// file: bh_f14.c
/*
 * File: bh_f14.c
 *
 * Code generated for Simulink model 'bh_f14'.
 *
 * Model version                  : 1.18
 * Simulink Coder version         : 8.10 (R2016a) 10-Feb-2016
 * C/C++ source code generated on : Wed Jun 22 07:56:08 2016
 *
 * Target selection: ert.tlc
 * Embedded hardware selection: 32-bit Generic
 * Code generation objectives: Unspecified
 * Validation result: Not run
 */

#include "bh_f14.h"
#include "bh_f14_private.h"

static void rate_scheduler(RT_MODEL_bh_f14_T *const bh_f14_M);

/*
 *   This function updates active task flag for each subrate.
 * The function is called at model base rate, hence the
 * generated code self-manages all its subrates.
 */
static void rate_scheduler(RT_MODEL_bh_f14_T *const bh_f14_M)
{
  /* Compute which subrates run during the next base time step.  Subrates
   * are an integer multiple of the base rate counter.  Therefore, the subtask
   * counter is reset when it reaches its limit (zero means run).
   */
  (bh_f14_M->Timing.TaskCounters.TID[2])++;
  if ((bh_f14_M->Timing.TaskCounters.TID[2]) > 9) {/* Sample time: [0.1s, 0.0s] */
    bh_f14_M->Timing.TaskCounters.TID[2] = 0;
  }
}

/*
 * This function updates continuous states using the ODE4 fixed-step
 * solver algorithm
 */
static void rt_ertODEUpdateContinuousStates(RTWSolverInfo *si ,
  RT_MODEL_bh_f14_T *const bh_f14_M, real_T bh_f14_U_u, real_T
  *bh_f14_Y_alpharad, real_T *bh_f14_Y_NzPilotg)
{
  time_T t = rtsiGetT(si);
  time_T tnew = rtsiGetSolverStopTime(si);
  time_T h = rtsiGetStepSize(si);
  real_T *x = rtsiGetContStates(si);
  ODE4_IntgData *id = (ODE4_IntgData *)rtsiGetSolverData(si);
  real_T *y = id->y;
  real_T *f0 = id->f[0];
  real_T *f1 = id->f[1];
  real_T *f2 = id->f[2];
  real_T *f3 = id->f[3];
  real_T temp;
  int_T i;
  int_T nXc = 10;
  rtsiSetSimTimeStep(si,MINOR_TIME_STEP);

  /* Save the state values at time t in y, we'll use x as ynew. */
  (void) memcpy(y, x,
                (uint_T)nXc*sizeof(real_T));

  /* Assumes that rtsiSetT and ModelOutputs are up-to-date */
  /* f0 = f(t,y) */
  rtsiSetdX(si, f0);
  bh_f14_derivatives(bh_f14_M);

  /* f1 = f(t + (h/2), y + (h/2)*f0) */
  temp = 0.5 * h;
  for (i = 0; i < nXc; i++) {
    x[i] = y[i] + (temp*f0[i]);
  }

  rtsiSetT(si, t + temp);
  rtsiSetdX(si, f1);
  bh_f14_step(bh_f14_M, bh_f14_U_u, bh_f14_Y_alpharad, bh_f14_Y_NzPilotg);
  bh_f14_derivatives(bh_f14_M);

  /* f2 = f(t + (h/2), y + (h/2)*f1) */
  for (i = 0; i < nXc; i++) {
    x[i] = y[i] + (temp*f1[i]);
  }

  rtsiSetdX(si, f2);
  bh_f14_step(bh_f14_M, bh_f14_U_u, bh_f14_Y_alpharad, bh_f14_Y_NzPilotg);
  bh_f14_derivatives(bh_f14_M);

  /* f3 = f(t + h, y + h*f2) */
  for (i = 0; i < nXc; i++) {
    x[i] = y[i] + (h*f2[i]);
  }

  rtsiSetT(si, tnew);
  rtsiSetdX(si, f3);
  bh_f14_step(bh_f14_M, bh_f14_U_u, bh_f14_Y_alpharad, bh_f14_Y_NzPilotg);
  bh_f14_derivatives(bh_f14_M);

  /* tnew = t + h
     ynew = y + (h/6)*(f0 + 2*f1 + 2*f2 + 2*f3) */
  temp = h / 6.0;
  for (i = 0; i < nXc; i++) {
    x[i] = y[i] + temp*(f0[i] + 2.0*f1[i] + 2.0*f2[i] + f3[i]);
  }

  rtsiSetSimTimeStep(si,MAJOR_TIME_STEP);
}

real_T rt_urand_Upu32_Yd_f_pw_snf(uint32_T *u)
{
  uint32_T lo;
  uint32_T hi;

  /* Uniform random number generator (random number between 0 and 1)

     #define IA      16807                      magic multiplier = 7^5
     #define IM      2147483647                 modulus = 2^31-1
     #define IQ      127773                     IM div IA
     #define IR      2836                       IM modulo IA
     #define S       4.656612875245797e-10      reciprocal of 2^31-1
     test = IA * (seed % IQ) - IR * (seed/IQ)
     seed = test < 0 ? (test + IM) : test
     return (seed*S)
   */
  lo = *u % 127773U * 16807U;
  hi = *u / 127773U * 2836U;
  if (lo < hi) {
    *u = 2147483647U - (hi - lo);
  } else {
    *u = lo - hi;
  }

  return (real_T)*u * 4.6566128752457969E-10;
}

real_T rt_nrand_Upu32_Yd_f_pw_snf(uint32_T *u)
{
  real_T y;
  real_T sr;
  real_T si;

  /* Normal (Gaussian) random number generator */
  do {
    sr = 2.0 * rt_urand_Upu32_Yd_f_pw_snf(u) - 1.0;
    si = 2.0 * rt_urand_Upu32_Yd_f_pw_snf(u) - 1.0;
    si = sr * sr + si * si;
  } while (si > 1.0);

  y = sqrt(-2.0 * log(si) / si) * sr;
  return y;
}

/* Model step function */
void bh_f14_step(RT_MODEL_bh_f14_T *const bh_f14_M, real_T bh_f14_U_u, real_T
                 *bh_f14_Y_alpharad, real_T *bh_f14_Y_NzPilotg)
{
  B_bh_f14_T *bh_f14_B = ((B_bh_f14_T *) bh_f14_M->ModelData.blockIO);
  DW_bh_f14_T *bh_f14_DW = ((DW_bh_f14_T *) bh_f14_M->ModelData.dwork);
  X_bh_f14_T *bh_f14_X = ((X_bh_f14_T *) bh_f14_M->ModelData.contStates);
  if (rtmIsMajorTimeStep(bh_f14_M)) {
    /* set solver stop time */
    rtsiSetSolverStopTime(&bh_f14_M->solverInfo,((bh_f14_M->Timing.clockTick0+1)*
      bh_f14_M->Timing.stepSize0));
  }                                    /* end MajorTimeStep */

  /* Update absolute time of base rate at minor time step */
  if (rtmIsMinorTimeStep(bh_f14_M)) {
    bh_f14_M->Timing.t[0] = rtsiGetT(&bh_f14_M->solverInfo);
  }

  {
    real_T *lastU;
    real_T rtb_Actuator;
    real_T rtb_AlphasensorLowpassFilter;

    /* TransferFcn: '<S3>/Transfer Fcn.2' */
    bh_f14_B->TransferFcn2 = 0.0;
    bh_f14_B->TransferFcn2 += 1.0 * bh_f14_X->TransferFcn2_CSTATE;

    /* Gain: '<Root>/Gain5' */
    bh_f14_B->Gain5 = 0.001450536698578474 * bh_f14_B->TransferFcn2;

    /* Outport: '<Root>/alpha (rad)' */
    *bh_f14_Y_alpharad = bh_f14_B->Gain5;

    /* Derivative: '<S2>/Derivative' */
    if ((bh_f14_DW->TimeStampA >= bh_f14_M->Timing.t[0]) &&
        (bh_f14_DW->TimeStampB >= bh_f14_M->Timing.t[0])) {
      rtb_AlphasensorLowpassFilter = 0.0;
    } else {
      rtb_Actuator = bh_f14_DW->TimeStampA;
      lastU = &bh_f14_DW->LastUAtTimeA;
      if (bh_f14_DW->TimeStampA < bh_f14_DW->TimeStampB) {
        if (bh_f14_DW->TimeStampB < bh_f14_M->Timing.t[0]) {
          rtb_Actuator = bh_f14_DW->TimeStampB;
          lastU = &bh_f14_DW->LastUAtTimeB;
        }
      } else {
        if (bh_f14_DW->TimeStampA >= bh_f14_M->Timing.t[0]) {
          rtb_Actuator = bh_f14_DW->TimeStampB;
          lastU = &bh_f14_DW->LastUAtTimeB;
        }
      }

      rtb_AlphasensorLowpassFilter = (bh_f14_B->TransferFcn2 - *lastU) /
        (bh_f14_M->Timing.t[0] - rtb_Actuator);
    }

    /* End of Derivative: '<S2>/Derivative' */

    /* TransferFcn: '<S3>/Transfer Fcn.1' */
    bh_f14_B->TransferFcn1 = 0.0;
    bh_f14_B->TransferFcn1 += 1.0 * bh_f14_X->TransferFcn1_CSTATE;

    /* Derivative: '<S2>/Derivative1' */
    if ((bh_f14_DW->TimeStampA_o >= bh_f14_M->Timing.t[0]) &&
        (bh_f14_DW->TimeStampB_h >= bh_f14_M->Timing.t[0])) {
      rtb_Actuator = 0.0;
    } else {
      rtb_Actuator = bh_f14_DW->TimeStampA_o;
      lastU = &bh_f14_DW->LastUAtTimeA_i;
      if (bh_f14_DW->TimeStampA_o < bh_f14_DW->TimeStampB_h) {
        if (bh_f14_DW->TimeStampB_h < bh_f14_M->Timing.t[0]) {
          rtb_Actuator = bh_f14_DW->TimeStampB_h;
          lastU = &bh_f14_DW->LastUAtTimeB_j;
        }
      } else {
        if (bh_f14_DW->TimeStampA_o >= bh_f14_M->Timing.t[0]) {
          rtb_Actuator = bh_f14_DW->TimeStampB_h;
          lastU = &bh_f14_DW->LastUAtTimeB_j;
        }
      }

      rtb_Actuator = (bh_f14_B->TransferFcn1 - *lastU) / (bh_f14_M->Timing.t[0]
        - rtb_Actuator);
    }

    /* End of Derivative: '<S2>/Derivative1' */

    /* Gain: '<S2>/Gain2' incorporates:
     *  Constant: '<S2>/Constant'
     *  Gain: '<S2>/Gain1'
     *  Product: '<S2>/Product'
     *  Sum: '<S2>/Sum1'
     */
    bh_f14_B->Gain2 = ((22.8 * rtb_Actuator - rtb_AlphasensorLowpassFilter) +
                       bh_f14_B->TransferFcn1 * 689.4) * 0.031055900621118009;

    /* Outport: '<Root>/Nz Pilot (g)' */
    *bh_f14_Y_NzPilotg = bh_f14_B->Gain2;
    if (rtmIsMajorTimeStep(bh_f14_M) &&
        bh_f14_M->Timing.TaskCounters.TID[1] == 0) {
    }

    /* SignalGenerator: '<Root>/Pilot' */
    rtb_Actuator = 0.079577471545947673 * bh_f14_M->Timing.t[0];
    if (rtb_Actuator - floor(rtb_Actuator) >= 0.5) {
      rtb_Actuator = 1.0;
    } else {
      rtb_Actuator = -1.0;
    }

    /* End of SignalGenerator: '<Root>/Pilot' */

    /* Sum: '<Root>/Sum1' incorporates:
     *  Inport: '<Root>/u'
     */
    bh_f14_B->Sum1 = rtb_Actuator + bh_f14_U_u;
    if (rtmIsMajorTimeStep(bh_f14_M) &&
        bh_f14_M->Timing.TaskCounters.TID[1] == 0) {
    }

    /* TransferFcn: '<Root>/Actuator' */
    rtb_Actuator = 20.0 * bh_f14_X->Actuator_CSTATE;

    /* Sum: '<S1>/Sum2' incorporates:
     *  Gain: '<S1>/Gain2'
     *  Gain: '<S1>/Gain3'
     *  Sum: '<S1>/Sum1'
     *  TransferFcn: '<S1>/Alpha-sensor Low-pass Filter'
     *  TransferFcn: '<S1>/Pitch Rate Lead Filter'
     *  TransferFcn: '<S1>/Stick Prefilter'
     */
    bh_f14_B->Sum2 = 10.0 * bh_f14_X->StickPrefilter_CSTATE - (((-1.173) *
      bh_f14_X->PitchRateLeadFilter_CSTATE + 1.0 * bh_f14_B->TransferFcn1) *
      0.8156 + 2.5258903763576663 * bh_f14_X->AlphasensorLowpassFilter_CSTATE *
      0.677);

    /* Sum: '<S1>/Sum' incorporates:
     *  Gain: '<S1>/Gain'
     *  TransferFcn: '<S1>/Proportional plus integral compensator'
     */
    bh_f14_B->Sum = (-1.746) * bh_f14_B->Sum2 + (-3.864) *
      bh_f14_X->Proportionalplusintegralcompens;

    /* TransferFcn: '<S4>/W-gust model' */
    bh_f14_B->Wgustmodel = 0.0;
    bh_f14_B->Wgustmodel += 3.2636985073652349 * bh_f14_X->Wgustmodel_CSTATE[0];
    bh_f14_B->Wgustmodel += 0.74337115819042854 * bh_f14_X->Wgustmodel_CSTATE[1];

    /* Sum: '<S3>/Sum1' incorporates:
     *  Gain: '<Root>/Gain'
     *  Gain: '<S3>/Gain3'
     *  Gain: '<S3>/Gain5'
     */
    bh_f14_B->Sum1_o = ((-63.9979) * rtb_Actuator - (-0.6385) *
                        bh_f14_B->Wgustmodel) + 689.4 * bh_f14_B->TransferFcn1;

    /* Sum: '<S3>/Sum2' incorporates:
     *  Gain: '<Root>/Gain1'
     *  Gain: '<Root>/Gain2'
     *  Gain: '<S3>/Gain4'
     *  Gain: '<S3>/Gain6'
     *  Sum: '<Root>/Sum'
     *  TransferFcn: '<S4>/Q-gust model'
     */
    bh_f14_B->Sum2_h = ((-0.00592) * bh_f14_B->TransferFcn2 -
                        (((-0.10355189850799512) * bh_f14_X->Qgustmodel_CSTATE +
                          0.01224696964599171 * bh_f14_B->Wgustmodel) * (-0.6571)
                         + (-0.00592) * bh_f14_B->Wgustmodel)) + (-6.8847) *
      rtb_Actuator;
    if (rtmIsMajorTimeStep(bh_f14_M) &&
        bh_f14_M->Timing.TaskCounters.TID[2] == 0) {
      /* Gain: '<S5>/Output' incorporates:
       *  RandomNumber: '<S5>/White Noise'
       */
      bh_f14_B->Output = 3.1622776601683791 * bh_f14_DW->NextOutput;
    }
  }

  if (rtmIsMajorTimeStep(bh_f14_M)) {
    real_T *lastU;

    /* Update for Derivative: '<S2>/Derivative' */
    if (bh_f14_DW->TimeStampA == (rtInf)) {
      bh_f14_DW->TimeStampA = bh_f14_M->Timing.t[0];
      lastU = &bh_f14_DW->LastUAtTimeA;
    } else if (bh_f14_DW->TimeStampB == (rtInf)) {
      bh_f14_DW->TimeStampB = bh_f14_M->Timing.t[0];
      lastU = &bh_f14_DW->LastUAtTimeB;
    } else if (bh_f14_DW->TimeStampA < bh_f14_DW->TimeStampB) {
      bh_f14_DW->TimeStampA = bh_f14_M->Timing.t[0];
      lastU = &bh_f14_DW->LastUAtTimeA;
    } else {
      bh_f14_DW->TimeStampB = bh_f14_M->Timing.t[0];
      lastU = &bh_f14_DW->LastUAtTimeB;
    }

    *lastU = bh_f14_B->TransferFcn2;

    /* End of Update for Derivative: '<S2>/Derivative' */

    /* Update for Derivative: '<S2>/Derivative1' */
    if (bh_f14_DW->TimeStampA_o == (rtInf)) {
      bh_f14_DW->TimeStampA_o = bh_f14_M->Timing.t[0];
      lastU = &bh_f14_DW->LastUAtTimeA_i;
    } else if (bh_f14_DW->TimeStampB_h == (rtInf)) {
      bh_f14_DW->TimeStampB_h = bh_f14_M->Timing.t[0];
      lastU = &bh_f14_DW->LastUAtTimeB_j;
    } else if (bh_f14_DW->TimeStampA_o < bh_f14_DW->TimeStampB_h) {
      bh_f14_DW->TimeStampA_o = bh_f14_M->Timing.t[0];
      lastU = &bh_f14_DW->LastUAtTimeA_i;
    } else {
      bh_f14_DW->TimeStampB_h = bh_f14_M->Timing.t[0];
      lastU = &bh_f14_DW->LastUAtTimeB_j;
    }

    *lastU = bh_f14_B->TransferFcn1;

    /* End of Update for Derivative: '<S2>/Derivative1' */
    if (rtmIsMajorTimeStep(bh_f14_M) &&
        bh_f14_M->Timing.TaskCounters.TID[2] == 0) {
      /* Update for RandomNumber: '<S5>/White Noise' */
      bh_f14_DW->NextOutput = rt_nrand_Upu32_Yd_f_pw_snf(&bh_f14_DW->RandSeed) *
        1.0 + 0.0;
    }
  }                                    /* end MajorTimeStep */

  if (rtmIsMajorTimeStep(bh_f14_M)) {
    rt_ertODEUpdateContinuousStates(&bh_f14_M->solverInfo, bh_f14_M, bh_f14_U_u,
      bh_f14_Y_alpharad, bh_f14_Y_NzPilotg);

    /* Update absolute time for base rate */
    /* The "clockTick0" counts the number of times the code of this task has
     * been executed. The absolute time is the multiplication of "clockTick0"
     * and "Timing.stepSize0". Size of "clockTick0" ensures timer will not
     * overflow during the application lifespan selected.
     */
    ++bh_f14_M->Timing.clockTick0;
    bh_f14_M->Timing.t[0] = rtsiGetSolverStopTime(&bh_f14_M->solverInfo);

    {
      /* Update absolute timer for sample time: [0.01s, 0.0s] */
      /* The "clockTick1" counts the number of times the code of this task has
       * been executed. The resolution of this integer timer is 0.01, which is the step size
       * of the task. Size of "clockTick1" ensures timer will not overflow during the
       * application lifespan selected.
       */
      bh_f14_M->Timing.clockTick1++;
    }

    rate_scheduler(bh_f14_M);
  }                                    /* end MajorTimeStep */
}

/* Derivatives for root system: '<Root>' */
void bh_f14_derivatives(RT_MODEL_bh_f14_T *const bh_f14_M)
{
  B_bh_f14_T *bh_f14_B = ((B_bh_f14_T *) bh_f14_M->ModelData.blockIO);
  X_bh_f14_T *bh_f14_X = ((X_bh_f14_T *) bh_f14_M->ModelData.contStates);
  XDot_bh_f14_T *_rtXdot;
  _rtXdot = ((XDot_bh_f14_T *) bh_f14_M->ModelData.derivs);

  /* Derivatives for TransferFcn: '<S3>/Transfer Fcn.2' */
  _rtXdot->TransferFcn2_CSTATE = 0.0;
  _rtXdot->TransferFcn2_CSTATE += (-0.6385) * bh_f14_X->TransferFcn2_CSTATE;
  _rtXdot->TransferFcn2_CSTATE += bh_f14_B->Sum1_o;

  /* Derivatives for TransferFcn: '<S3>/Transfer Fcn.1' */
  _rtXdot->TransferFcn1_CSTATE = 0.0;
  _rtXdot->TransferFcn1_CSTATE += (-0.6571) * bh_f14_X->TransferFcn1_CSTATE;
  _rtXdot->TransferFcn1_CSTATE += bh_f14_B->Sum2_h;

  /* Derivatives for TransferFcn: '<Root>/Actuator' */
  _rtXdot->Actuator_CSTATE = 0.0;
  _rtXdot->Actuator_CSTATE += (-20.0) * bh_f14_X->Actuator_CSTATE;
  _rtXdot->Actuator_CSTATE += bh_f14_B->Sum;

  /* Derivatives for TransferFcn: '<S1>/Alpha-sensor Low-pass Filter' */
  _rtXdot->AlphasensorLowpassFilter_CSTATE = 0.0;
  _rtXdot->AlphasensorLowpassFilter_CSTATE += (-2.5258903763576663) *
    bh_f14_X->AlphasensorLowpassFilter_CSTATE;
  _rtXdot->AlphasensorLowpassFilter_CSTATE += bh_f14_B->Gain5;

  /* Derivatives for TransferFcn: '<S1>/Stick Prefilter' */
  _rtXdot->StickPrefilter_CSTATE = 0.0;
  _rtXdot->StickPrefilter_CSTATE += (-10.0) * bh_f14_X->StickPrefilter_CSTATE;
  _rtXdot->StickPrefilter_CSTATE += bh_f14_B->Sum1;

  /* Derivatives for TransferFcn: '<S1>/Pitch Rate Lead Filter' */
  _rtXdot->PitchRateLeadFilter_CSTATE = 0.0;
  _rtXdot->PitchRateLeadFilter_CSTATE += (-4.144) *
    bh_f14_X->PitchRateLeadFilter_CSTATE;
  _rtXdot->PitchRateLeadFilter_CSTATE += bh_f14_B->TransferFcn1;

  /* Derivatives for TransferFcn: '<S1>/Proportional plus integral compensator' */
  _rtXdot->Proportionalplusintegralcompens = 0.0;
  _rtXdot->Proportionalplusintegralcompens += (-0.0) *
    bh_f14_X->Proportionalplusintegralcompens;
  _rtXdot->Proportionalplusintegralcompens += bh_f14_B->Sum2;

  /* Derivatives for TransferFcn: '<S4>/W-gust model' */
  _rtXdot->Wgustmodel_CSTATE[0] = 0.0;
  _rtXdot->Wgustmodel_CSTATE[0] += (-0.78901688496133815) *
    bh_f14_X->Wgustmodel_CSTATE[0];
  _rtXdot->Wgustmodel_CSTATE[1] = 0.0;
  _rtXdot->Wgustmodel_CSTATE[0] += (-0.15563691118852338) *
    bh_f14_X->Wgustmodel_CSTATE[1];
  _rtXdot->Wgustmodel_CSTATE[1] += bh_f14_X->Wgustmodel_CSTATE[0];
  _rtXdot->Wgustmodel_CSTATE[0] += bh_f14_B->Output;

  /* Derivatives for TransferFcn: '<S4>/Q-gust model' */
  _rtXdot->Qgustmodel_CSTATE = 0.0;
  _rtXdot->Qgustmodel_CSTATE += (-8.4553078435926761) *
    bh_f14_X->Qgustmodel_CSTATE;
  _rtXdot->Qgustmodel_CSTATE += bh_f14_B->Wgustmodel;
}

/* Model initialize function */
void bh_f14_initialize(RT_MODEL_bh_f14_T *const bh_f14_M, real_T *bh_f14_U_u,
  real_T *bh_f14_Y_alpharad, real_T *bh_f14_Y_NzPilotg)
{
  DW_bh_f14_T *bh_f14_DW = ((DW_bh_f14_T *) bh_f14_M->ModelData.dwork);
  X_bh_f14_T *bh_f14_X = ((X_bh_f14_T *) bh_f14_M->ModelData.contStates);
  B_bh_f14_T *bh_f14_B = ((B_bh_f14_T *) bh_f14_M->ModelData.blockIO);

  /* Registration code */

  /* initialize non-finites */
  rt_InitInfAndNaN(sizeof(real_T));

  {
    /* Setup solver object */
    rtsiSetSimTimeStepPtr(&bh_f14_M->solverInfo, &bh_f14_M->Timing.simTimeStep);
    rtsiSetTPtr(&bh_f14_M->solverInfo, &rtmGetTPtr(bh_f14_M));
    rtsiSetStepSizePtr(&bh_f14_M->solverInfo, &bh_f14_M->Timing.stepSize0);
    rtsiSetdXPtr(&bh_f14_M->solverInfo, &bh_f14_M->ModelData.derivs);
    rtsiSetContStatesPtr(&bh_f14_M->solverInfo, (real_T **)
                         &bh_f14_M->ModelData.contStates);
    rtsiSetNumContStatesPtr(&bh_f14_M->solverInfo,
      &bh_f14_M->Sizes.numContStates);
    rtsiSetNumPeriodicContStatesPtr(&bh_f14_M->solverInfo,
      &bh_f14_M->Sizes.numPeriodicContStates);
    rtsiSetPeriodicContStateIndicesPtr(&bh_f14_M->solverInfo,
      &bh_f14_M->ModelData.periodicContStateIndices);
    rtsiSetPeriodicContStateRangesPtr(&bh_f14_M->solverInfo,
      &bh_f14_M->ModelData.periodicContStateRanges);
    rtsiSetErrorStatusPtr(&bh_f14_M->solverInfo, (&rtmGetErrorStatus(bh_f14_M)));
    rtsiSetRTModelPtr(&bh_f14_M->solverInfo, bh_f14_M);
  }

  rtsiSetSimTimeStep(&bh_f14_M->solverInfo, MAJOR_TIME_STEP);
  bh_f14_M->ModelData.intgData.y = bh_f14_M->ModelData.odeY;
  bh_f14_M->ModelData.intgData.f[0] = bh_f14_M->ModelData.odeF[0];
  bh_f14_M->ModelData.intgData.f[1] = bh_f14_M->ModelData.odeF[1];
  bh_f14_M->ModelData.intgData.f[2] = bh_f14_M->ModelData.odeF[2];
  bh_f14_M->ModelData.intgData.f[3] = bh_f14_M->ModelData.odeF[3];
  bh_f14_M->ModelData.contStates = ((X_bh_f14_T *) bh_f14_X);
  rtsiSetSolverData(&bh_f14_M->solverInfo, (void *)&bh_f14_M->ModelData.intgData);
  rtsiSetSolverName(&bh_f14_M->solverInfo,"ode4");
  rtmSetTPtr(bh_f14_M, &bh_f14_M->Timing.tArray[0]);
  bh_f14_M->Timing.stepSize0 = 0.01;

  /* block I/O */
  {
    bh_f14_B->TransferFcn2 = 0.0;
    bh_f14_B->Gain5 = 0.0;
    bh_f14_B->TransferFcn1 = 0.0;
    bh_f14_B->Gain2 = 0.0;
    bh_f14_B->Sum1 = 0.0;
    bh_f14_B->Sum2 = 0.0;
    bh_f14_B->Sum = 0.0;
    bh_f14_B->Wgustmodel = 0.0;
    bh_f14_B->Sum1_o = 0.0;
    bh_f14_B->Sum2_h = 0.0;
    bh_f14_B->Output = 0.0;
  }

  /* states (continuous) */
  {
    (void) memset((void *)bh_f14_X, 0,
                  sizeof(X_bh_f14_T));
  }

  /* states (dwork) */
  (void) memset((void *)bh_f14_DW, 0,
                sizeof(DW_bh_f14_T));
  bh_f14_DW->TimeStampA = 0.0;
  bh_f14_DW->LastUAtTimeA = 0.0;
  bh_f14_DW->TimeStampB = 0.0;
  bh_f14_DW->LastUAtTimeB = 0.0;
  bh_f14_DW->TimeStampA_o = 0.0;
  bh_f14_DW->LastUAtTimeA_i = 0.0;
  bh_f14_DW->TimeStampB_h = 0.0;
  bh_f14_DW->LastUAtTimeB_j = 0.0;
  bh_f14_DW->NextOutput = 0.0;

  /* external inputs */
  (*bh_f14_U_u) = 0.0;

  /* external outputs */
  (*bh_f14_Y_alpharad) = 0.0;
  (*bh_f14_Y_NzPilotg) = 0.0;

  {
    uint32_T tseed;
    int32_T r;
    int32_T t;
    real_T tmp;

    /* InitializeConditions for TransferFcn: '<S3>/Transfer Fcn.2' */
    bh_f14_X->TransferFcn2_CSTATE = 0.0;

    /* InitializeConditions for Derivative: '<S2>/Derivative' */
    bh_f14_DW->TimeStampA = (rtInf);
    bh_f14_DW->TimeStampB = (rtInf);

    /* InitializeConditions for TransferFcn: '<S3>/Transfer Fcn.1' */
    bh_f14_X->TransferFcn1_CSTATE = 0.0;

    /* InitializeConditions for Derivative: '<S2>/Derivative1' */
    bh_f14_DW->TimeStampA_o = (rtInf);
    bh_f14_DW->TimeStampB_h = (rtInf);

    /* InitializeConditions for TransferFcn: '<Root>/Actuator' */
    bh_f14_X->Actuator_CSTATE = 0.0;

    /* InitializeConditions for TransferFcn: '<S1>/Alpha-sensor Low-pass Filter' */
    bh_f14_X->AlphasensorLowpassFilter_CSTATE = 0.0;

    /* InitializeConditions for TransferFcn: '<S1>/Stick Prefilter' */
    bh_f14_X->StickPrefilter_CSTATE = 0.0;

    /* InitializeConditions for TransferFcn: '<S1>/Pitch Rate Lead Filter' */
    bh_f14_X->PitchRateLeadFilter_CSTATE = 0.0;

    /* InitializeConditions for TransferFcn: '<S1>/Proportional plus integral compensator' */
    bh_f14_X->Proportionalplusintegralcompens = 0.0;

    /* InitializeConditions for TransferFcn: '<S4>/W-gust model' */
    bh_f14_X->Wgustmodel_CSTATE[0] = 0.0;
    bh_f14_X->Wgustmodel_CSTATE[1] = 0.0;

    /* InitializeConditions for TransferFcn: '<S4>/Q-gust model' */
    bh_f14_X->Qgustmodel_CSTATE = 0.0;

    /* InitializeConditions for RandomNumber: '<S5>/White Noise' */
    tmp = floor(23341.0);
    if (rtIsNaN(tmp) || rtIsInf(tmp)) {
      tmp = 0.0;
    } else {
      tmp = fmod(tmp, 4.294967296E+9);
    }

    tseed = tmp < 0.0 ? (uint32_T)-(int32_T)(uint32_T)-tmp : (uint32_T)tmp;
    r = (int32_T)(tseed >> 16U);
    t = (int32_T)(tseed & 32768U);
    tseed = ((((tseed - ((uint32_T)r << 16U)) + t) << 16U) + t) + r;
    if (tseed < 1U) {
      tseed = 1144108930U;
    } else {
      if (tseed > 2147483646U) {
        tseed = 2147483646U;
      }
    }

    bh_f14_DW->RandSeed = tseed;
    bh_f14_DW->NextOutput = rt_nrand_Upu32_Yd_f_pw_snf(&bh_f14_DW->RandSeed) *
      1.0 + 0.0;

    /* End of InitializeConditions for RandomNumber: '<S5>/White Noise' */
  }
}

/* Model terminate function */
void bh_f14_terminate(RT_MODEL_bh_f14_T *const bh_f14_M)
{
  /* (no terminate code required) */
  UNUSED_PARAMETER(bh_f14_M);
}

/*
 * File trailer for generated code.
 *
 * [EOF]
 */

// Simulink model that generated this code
simulink model "bh_f14"  (R2016a)
settings: Solver=ode4  SolverMode=SingleTasking  StartTime=0.0  StopTime=60  FixedStep=0.01  RelTol=1e-4  AbsTol=1e-6
PreLoadFcn:
  | f14dat
undefined symbols (not defined in the file or in its folder): a, b, g, Ka, Kf, Ki, Kq, Md, Mq, Mw, Swg, Ta, Tal, Ts, Uo, Vto, W1, W2, Zd, Zw
libraries: simulink x1

== system bh_f14 ==
  note: F-14 Flight Control
  note: Copyright 1990-2014 The MathWorks, Inc.
  u : Inport
  Actuator : TransferFcn  Denominator=[ Ta, 1]
  Angle of Attack : Scope
  Controller : Subsystem
  Gain : Gain  Gain=Zw  SaturateOnIntegerOverflow=on  OutDataTypeStr=Inherit: Same as input  ParamDataTypeStr=Inherit: Same as input
  Gain1 : Gain  Gain=Mq  SaturateOnIntegerOverflow=on  OutDataTypeStr=Inherit: Same as input  ParamDataTypeStr=Inherit: Same as input
  Gain2 : Gain  Gain=Mw  SaturateOnIntegerOverflow=on  OutDataTypeStr=Inherit: Same as input  ParamDataTypeStr=Inherit: Same as input
  Gain5 : Gain  Gain=1/Uo  SaturateOnIntegerOverflow=on  OutDataTypeStr=Inherit: Same as input  ParamDataTypeStr=Inherit: Same as input
  Nz pilot calculation : Subsystem
  Pilot : SignalGenerator  WaveForm=square  Frequency=0.500000  Units=rad/sec
  Pilot G force Scope : Scope
  Plant : Subsystem
  Stick Input : Scope
  Sum : Sum  Inputs=|++  SaturateOnIntegerOverflow=on  InputSameDT=on  OutDataTypeStr=Inherit: Same as first input
  Sum1 : Sum  Inputs=|++  SaturateOnIntegerOverflow=on  InputSameDT=on  OutDataTypeStr=Inherit: Same as first input
  Wind : Subsystem
  alpha (rad) : Outport  InitialOutput=0
  Nz Pilot (g) : Outport  Port=2  InitialOutput=0
  wires:
  Gain5/1 -> alpha (rad)/1, Angle of Attack/1, Controller/2(alpha (rad))
  Plant/1(Vertical Velocity w (ft/sec)) -> Gain5/1, Nz pilot calculation/1(w)  "w"
  Nz pilot calculation/1(Pilot g force (g)) -> Pilot G force Scope/1, Nz Pilot (g)/1
  Gain2/1 -> Sum/1
  Gain/1 -> Plant/2(Vertical Gust wGust (ft/sec))
  Pilot/1 -> Sum1/1
  u/1 -> Sum1/2
  Wind/2(Qg) -> Gain1/1  "qGust"
  Wind/1(Wg) -> Gain2/1, Gain/1  "wGust"
  Sum/1 -> Plant/3(Rotary Gust qGust (rad/sec))
  Gain1/1 -> Sum/2
  Plant/2(Pitch Rate q (rad/sec)) -> Nz pilot calculation/2(q), Controller/3(q (rad/sec))  "q"
  Actuator/1 -> Plant/1(Elevator Deflection d (deg))
  Controller/1(Elevator Command (deg)) -> Actuator/1
  Sum1/1 -> Stick Input/1, Controller/1(Stick Input (in))

== system bh_f14/Controller ==
  Stick Input (in) : Inport
  alpha (rad) : Inport  Port=2
  q (rad/sec) : Inport  Port=3
  Alpha-sensor Low-pass Filter : TransferFcn  Denominator=[Tal,1]
  Gain : Gain  Gain=Kf  SaturateOnIntegerOverflow=on  OutDataTypeStr=Inherit: Same as input  ParamDataTypeStr=Inherit: Same as input
  Gain2 : Gain  Gain=Kq  SaturateOnIntegerOverflow=on  OutDataTypeStr=Inherit: Same as input  ParamDataTypeStr=Inherit: Same as input
  Gain3 : Gain  Gain=Ka  SaturateOnIntegerOverflow=on  OutDataTypeStr=Inherit: Same as input  ParamDataTypeStr=Inherit: Same as input
  Pitch Rate Lead Filter : TransferFcn  Numerator=[1,W1]  Denominator=[1,W2]
  Proportional plus integral compensator : TransferFcn  Numerator=[Ki]  Denominator=[1,0]
  Stick Prefilter : TransferFcn  Denominator=[Ts,1]
  Sum : Sum  Inputs=++|  SaturateOnIntegerOverflow=on  InputSameDT=on  OutDataTypeStr=Inherit: Same as first input
  Sum1 : Sum  Inputs=|++  SaturateOnIntegerOverflow=on  InputSameDT=on  OutDataTypeStr=Inherit: Same as first input
  Sum2 : Sum  Inputs=|+-  SaturateOnIntegerOverflow=on  InputSameDT=on  OutDataTypeStr=Inherit: Same as first input
  Elevator Command (deg) : Outport  InitialOutput=0
  wires:
  Sum2/1 -> Proportional plus integral compensator/1, Gain/1
  Gain/1 -> Sum/1
  Proportional plus integral compensator/1 -> Sum/2
  Stick Prefilter/1 -> Sum2/1
  Sum/1 -> Elevator Command (deg)/1
  Gain2/1 -> Sum1/1
  Gain3/1 -> Sum1/2
  Sum1/1 -> Sum2/2
  Pitch Rate Lead Filter/1 -> Gain2/1
  q (rad/sec)/1 -> Pitch Rate Lead Filter/1
  Alpha-sensor Low-pass Filter/1 -> Gain3/1
  alpha (rad)/1 -> Alpha-sensor Low-pass Filter/1
  Stick Input (in)/1 -> Stick Prefilter/1

== system bh_f14/Nz pilot calculation ==
  note: Nz pilot calculation
  note: Nz = (dq/dt*22.8 + q*Uo - dw/dt)/g
  w : Inport
  q : Inport  Port=2
  Constant : Constant  Value=Uo
  Derivative : Derivative
  Derivative1 : Derivative
  Gain1 : Gain  Gain=22.8  SaturateOnIntegerOverflow=on  OutDataTypeStr=Inherit: Same as input  ParamDataTypeStr=Inherit: Same as input
  Gain2 : Gain  Gain=1/g  SaturateOnIntegerOverflow=on  OutDataTypeStr=Inherit: Same as input  ParamDataTypeStr=Inherit: Same as input
  Product : Product  SaturateOnIntegerOverflow=on  RndMeth=Zero  InputSameDT=on  OutDataTypeStr=Inherit: Same as first input
  Sum1 : Sum  Inputs=-++  SaturateOnIntegerOverflow=on  InputSameDT=on  OutDataTypeStr=Inherit: Same as first input
  Pilot g force (g) : Outport  InitialOutput=0
  wires:
  q/1 -> Product/1, Derivative1/1
  Constant/1 -> Product/2
  Gain2/1 -> Pilot g force (g)/1
  Sum1/1 -> Gain2/1
  Derivative1/1 -> Gain1/1
  Gain1/1 -> Sum1/2
  Product/1 -> Sum1/3
  Derivative/1 -> Sum1/1
  w/1 -> Derivative/1

== system bh_f14/Plant ==
  Elevator Deflection d (deg) : Inport
  Vertical Gust wGust (ft/sec) : Inport  Port=2
  Rotary Gust qGust (rad/sec) : Inport  Port=3
  Gain3 : Gain  Gain=Uo  SaturateOnIntegerOverflow=on  OutDataTypeStr=Inherit: Same as input  ParamDataTypeStr=Inherit: Same as input
  Gain4 : Gain  Gain=Mw  SaturateOnIntegerOverflow=on  OutDataTypeStr=Inherit: Same as input  ParamDataTypeStr=Inherit: Same as input
  Gain5 : Gain  Gain=Zd  SaturateOnIntegerOverflow=on  OutDataTypeStr=Inherit: Same as input  ParamDataTypeStr=Inherit: Same as input
  Gain6 : Gain  Gain=Md  SaturateOnIntegerOverflow=on  OutDataTypeStr=Inherit: Same as input  ParamDataTypeStr=Inherit: Same as input
  Sum1 : Sum  Inputs=+-+  SaturateOnIntegerOverflow=on  InputSameDT=on  OutDataTypeStr=Inherit: Same as first input
  Sum2 : Sum  Inputs=+-+  SaturateOnIntegerOverflow=on  InputSameDT=on  OutDataTypeStr=Inherit: Same as first input
  Transfer Fcn.1 : TransferFcn  Denominator=[1,-Mq]
  Transfer Fcn.2 : TransferFcn  Denominator=[1,-Zw]
  Vertical Velocity w (ft/sec) : Outport  InitialOutput=0
  Pitch Rate q (rad/sec) : Outport  Port=2  InitialOutput=0
  wires:
  Transfer Fcn.2/1 -> Vertical Velocity w (ft/sec)/1, Gain4/1
  Transfer Fcn.1/1 -> Pitch Rate q (rad/sec)/1, Gain3/1
  Gain6/1 -> Sum2/3
  Gain5/1 -> Sum1/1
  Gain3/1 -> Sum1/3
  Rotary Gust qGust (rad/sec)/1 -> Sum2/2
  Sum2/1 -> Transfer Fcn.1/1
  Sum1/1 -> Transfer Fcn.2/1
  Gain4/1 -> Sum2/1
  Vertical Gust wGust (ft/sec)/1 -> Sum1/2
  Elevator Deflection d (deg)/1 -> Gain5/1, Gain6/1

== system bh_f14/Wind ==
  Band-Limited White Noise : simulink/Sources/Band-Limited White Noise  Cov=1  Ts=0.1  seed=[23341]
  Q-gust model : TransferFcn  Numerator=pi/(4*b)*[1 0]  Denominator=[1 pi*Vto/(4*b)]
  W-gust model : TransferFcn  Numerator=Swg/sqrt(a^3)*[sqrt(3)*a,1]  Denominator=[1 (2/a) 1/a^2]
  Wg : Outport  InitialOutput=0
  Qg : Outport  Port=2  InitialOutput=0
  wires:
  Band-Limited White Noise/1 -> W-gust model/1
  Q-gust model/1 -> Qg/1
  W-gust model/1 -> Wg/1, Q-gust model/1
